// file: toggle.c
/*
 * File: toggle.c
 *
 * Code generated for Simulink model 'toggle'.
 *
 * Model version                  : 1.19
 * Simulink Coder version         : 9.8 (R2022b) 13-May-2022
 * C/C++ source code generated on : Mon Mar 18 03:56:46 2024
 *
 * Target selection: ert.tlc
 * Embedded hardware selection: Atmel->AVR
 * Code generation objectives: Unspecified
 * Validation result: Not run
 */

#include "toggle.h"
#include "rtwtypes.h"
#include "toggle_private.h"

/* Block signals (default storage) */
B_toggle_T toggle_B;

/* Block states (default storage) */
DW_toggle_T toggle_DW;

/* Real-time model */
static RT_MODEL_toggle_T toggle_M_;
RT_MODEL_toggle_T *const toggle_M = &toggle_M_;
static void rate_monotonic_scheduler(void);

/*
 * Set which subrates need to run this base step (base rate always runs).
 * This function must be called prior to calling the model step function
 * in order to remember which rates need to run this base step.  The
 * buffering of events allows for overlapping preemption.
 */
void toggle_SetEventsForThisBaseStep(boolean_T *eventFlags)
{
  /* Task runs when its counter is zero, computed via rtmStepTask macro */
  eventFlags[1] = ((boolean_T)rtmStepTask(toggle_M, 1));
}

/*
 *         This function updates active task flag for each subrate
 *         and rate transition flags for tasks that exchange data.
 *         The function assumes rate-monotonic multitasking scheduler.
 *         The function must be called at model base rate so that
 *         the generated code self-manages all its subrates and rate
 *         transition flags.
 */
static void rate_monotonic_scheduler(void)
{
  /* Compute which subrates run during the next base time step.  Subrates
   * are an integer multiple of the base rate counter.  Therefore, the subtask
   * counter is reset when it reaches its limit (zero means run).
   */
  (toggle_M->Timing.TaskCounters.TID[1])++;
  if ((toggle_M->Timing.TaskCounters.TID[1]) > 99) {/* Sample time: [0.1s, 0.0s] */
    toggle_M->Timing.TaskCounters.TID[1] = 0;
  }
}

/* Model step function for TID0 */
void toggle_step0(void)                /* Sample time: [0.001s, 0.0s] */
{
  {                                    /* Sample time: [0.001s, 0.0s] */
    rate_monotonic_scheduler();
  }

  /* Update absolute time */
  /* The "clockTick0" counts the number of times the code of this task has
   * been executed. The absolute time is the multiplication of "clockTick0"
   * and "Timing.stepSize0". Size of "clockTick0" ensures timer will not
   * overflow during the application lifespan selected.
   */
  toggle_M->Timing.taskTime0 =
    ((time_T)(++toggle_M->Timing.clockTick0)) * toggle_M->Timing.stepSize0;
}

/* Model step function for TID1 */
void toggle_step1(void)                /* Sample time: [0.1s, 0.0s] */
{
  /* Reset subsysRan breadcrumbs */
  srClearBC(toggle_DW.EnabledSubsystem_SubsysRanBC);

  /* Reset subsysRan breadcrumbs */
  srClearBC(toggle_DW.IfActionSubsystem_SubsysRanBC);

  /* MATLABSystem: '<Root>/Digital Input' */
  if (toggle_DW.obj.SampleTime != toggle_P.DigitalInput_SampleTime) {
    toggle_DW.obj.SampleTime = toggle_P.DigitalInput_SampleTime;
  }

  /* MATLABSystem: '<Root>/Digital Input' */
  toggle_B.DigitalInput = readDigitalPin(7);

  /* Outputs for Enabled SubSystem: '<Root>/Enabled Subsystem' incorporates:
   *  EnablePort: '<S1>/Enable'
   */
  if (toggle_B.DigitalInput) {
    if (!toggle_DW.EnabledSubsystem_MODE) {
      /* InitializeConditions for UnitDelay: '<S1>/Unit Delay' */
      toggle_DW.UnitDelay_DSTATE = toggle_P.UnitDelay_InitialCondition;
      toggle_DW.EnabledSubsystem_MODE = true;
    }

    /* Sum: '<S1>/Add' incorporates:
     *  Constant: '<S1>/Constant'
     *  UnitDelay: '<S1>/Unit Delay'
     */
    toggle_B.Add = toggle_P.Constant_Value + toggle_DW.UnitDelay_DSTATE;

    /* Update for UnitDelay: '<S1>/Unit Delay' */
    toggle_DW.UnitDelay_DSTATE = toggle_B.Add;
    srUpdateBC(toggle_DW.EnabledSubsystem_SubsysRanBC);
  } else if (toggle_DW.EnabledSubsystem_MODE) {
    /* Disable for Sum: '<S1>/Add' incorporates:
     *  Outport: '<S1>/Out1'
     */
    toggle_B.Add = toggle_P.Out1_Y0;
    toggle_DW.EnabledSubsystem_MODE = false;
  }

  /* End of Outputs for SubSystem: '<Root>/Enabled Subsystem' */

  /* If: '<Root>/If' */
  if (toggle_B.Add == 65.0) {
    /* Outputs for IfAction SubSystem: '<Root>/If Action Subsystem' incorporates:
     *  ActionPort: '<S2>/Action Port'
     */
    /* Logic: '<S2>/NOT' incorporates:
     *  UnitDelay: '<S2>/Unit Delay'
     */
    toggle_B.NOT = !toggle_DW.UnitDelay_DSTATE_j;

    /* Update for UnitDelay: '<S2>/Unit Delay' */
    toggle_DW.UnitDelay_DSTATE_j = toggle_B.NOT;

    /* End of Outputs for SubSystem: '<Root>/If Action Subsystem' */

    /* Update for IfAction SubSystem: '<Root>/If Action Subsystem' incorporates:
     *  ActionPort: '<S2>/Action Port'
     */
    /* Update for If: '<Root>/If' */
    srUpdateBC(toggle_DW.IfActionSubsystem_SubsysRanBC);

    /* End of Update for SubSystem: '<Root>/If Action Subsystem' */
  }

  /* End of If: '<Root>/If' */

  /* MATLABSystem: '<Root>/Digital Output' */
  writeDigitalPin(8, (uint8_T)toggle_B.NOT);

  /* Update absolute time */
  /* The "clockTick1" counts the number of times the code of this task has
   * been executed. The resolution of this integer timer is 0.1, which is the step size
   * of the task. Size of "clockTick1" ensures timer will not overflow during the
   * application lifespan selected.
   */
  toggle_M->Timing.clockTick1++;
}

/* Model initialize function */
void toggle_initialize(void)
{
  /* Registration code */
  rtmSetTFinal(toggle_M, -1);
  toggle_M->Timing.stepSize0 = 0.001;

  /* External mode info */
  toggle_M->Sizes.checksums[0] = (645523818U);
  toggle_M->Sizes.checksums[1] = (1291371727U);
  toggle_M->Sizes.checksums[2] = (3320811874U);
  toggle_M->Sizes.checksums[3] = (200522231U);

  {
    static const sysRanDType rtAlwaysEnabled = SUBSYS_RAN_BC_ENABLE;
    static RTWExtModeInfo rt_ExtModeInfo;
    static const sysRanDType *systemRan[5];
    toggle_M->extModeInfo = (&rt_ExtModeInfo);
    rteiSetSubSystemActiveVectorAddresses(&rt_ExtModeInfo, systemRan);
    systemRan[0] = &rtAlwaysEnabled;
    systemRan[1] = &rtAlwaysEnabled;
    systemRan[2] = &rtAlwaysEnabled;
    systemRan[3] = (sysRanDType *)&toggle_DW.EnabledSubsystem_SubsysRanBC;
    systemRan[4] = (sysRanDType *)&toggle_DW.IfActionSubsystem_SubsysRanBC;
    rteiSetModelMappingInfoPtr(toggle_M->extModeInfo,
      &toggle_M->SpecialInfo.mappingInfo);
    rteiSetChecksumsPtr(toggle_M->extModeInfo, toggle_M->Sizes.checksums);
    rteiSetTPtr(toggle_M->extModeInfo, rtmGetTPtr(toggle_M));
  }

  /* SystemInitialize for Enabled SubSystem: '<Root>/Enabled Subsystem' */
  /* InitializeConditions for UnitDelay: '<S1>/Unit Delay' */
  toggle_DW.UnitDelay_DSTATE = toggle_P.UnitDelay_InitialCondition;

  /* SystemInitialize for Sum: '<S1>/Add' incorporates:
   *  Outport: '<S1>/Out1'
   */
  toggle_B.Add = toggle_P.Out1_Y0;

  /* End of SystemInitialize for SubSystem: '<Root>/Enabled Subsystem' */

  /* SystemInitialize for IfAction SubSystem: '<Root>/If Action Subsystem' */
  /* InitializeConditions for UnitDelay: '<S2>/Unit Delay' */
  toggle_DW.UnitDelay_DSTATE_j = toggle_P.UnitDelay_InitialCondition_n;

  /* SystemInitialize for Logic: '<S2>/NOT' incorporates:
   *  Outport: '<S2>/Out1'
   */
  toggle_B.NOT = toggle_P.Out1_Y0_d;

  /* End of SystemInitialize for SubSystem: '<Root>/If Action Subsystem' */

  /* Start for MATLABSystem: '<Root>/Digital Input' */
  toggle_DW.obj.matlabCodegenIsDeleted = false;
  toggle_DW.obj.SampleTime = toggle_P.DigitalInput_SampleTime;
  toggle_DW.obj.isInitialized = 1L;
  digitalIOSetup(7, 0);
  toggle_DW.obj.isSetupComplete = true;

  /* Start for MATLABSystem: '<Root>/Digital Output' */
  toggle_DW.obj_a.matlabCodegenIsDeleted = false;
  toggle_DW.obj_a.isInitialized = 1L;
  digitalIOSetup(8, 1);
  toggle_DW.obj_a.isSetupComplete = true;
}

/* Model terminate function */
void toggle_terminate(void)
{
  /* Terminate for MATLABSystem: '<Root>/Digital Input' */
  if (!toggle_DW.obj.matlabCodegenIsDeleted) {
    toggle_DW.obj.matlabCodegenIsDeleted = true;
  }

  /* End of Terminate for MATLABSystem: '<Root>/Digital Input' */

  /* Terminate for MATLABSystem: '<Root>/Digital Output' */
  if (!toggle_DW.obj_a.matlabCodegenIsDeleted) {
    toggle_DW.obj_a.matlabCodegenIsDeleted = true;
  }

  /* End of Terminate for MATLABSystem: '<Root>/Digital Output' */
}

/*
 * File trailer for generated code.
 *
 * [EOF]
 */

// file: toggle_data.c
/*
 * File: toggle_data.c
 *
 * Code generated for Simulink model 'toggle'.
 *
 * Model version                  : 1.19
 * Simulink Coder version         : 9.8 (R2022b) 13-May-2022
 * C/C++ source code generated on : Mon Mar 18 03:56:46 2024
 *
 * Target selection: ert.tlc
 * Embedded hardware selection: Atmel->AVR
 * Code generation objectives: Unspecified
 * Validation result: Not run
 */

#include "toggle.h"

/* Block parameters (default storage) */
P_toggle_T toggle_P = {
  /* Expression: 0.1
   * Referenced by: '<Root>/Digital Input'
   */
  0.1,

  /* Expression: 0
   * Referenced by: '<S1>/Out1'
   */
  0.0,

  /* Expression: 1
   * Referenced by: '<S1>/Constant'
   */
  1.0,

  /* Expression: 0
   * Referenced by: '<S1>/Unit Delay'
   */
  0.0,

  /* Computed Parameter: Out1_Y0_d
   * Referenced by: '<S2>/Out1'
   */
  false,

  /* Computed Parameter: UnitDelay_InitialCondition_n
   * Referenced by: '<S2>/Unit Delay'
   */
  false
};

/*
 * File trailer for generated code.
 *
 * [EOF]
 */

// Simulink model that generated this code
simulink model "toggle"  (R2022b)
settings: Solver=FixedStepDiscrete  StartTime=0.0  StopTime=inf  FixedStep=1e-3  RelTol=1e-3  EnableMultiTasking=on
libraries: arduinolib x2

== system toggle ==
  Digital Input : arduinolib/Digital Input  pinNumber=7  mode=Default  Direction=input  SampleTime=0.1  blockPlatform=arduino
  Digital Output : arduinolib/Digital Output  pinNumber=8  Direction=output  blockPlatform=arduino
  Enabled Subsystem : Subsystem  TreatAsAtomicUnit=on
  If : If  IfExpression=u1 == 65  ShowElse=off
  If Action Subsystem : Subsystem  TreatAsAtomicUnit=on
  Scope : Scope  NumInputPorts=3
  wires:
  If/1 -> If Action Subsystem/Action
  Enabled Subsystem/1(Out1) -> Scope/2, If/1
  Digital Input/1 -> Enabled Subsystem/Enable, Scope/1
  If Action Subsystem/1(Out1) -> Digital Output/1, Scope/3

== system toggle/Enabled Subsystem ==
  Enable : EnablePort  StatesWhenEnabling=reset
  Add : Sum
  Constant : Constant
  Unit Delay : UnitDelay  SampleTime=-1  HasFrameUpgradeWarning=on
  Out1 : Outport  OutputWhenDisabled=reset  InitialOutput=0
  wires:
  Constant/1 -> Add/1
  Unit Delay/1 -> Add/2
  Add/1 -> Unit Delay/1, Out1/1

== system toggle/If Action Subsystem ==
  Action Port : ActionPort  ActionPortLabel=if(u1 == 10)
  NOT : Logic  Operator=NOT  IconShape=distinctive  AllPortsSameDT=off  OutDataTypeStr=boolean
  Unit Delay : UnitDelay  SampleTime=-1  HasFrameUpgradeWarning=on
  Out1 : Outport
  wires:
  NOT/1 -> Unit Delay/1, Out1/1
  Unit Delay/1 -> NOT/1
